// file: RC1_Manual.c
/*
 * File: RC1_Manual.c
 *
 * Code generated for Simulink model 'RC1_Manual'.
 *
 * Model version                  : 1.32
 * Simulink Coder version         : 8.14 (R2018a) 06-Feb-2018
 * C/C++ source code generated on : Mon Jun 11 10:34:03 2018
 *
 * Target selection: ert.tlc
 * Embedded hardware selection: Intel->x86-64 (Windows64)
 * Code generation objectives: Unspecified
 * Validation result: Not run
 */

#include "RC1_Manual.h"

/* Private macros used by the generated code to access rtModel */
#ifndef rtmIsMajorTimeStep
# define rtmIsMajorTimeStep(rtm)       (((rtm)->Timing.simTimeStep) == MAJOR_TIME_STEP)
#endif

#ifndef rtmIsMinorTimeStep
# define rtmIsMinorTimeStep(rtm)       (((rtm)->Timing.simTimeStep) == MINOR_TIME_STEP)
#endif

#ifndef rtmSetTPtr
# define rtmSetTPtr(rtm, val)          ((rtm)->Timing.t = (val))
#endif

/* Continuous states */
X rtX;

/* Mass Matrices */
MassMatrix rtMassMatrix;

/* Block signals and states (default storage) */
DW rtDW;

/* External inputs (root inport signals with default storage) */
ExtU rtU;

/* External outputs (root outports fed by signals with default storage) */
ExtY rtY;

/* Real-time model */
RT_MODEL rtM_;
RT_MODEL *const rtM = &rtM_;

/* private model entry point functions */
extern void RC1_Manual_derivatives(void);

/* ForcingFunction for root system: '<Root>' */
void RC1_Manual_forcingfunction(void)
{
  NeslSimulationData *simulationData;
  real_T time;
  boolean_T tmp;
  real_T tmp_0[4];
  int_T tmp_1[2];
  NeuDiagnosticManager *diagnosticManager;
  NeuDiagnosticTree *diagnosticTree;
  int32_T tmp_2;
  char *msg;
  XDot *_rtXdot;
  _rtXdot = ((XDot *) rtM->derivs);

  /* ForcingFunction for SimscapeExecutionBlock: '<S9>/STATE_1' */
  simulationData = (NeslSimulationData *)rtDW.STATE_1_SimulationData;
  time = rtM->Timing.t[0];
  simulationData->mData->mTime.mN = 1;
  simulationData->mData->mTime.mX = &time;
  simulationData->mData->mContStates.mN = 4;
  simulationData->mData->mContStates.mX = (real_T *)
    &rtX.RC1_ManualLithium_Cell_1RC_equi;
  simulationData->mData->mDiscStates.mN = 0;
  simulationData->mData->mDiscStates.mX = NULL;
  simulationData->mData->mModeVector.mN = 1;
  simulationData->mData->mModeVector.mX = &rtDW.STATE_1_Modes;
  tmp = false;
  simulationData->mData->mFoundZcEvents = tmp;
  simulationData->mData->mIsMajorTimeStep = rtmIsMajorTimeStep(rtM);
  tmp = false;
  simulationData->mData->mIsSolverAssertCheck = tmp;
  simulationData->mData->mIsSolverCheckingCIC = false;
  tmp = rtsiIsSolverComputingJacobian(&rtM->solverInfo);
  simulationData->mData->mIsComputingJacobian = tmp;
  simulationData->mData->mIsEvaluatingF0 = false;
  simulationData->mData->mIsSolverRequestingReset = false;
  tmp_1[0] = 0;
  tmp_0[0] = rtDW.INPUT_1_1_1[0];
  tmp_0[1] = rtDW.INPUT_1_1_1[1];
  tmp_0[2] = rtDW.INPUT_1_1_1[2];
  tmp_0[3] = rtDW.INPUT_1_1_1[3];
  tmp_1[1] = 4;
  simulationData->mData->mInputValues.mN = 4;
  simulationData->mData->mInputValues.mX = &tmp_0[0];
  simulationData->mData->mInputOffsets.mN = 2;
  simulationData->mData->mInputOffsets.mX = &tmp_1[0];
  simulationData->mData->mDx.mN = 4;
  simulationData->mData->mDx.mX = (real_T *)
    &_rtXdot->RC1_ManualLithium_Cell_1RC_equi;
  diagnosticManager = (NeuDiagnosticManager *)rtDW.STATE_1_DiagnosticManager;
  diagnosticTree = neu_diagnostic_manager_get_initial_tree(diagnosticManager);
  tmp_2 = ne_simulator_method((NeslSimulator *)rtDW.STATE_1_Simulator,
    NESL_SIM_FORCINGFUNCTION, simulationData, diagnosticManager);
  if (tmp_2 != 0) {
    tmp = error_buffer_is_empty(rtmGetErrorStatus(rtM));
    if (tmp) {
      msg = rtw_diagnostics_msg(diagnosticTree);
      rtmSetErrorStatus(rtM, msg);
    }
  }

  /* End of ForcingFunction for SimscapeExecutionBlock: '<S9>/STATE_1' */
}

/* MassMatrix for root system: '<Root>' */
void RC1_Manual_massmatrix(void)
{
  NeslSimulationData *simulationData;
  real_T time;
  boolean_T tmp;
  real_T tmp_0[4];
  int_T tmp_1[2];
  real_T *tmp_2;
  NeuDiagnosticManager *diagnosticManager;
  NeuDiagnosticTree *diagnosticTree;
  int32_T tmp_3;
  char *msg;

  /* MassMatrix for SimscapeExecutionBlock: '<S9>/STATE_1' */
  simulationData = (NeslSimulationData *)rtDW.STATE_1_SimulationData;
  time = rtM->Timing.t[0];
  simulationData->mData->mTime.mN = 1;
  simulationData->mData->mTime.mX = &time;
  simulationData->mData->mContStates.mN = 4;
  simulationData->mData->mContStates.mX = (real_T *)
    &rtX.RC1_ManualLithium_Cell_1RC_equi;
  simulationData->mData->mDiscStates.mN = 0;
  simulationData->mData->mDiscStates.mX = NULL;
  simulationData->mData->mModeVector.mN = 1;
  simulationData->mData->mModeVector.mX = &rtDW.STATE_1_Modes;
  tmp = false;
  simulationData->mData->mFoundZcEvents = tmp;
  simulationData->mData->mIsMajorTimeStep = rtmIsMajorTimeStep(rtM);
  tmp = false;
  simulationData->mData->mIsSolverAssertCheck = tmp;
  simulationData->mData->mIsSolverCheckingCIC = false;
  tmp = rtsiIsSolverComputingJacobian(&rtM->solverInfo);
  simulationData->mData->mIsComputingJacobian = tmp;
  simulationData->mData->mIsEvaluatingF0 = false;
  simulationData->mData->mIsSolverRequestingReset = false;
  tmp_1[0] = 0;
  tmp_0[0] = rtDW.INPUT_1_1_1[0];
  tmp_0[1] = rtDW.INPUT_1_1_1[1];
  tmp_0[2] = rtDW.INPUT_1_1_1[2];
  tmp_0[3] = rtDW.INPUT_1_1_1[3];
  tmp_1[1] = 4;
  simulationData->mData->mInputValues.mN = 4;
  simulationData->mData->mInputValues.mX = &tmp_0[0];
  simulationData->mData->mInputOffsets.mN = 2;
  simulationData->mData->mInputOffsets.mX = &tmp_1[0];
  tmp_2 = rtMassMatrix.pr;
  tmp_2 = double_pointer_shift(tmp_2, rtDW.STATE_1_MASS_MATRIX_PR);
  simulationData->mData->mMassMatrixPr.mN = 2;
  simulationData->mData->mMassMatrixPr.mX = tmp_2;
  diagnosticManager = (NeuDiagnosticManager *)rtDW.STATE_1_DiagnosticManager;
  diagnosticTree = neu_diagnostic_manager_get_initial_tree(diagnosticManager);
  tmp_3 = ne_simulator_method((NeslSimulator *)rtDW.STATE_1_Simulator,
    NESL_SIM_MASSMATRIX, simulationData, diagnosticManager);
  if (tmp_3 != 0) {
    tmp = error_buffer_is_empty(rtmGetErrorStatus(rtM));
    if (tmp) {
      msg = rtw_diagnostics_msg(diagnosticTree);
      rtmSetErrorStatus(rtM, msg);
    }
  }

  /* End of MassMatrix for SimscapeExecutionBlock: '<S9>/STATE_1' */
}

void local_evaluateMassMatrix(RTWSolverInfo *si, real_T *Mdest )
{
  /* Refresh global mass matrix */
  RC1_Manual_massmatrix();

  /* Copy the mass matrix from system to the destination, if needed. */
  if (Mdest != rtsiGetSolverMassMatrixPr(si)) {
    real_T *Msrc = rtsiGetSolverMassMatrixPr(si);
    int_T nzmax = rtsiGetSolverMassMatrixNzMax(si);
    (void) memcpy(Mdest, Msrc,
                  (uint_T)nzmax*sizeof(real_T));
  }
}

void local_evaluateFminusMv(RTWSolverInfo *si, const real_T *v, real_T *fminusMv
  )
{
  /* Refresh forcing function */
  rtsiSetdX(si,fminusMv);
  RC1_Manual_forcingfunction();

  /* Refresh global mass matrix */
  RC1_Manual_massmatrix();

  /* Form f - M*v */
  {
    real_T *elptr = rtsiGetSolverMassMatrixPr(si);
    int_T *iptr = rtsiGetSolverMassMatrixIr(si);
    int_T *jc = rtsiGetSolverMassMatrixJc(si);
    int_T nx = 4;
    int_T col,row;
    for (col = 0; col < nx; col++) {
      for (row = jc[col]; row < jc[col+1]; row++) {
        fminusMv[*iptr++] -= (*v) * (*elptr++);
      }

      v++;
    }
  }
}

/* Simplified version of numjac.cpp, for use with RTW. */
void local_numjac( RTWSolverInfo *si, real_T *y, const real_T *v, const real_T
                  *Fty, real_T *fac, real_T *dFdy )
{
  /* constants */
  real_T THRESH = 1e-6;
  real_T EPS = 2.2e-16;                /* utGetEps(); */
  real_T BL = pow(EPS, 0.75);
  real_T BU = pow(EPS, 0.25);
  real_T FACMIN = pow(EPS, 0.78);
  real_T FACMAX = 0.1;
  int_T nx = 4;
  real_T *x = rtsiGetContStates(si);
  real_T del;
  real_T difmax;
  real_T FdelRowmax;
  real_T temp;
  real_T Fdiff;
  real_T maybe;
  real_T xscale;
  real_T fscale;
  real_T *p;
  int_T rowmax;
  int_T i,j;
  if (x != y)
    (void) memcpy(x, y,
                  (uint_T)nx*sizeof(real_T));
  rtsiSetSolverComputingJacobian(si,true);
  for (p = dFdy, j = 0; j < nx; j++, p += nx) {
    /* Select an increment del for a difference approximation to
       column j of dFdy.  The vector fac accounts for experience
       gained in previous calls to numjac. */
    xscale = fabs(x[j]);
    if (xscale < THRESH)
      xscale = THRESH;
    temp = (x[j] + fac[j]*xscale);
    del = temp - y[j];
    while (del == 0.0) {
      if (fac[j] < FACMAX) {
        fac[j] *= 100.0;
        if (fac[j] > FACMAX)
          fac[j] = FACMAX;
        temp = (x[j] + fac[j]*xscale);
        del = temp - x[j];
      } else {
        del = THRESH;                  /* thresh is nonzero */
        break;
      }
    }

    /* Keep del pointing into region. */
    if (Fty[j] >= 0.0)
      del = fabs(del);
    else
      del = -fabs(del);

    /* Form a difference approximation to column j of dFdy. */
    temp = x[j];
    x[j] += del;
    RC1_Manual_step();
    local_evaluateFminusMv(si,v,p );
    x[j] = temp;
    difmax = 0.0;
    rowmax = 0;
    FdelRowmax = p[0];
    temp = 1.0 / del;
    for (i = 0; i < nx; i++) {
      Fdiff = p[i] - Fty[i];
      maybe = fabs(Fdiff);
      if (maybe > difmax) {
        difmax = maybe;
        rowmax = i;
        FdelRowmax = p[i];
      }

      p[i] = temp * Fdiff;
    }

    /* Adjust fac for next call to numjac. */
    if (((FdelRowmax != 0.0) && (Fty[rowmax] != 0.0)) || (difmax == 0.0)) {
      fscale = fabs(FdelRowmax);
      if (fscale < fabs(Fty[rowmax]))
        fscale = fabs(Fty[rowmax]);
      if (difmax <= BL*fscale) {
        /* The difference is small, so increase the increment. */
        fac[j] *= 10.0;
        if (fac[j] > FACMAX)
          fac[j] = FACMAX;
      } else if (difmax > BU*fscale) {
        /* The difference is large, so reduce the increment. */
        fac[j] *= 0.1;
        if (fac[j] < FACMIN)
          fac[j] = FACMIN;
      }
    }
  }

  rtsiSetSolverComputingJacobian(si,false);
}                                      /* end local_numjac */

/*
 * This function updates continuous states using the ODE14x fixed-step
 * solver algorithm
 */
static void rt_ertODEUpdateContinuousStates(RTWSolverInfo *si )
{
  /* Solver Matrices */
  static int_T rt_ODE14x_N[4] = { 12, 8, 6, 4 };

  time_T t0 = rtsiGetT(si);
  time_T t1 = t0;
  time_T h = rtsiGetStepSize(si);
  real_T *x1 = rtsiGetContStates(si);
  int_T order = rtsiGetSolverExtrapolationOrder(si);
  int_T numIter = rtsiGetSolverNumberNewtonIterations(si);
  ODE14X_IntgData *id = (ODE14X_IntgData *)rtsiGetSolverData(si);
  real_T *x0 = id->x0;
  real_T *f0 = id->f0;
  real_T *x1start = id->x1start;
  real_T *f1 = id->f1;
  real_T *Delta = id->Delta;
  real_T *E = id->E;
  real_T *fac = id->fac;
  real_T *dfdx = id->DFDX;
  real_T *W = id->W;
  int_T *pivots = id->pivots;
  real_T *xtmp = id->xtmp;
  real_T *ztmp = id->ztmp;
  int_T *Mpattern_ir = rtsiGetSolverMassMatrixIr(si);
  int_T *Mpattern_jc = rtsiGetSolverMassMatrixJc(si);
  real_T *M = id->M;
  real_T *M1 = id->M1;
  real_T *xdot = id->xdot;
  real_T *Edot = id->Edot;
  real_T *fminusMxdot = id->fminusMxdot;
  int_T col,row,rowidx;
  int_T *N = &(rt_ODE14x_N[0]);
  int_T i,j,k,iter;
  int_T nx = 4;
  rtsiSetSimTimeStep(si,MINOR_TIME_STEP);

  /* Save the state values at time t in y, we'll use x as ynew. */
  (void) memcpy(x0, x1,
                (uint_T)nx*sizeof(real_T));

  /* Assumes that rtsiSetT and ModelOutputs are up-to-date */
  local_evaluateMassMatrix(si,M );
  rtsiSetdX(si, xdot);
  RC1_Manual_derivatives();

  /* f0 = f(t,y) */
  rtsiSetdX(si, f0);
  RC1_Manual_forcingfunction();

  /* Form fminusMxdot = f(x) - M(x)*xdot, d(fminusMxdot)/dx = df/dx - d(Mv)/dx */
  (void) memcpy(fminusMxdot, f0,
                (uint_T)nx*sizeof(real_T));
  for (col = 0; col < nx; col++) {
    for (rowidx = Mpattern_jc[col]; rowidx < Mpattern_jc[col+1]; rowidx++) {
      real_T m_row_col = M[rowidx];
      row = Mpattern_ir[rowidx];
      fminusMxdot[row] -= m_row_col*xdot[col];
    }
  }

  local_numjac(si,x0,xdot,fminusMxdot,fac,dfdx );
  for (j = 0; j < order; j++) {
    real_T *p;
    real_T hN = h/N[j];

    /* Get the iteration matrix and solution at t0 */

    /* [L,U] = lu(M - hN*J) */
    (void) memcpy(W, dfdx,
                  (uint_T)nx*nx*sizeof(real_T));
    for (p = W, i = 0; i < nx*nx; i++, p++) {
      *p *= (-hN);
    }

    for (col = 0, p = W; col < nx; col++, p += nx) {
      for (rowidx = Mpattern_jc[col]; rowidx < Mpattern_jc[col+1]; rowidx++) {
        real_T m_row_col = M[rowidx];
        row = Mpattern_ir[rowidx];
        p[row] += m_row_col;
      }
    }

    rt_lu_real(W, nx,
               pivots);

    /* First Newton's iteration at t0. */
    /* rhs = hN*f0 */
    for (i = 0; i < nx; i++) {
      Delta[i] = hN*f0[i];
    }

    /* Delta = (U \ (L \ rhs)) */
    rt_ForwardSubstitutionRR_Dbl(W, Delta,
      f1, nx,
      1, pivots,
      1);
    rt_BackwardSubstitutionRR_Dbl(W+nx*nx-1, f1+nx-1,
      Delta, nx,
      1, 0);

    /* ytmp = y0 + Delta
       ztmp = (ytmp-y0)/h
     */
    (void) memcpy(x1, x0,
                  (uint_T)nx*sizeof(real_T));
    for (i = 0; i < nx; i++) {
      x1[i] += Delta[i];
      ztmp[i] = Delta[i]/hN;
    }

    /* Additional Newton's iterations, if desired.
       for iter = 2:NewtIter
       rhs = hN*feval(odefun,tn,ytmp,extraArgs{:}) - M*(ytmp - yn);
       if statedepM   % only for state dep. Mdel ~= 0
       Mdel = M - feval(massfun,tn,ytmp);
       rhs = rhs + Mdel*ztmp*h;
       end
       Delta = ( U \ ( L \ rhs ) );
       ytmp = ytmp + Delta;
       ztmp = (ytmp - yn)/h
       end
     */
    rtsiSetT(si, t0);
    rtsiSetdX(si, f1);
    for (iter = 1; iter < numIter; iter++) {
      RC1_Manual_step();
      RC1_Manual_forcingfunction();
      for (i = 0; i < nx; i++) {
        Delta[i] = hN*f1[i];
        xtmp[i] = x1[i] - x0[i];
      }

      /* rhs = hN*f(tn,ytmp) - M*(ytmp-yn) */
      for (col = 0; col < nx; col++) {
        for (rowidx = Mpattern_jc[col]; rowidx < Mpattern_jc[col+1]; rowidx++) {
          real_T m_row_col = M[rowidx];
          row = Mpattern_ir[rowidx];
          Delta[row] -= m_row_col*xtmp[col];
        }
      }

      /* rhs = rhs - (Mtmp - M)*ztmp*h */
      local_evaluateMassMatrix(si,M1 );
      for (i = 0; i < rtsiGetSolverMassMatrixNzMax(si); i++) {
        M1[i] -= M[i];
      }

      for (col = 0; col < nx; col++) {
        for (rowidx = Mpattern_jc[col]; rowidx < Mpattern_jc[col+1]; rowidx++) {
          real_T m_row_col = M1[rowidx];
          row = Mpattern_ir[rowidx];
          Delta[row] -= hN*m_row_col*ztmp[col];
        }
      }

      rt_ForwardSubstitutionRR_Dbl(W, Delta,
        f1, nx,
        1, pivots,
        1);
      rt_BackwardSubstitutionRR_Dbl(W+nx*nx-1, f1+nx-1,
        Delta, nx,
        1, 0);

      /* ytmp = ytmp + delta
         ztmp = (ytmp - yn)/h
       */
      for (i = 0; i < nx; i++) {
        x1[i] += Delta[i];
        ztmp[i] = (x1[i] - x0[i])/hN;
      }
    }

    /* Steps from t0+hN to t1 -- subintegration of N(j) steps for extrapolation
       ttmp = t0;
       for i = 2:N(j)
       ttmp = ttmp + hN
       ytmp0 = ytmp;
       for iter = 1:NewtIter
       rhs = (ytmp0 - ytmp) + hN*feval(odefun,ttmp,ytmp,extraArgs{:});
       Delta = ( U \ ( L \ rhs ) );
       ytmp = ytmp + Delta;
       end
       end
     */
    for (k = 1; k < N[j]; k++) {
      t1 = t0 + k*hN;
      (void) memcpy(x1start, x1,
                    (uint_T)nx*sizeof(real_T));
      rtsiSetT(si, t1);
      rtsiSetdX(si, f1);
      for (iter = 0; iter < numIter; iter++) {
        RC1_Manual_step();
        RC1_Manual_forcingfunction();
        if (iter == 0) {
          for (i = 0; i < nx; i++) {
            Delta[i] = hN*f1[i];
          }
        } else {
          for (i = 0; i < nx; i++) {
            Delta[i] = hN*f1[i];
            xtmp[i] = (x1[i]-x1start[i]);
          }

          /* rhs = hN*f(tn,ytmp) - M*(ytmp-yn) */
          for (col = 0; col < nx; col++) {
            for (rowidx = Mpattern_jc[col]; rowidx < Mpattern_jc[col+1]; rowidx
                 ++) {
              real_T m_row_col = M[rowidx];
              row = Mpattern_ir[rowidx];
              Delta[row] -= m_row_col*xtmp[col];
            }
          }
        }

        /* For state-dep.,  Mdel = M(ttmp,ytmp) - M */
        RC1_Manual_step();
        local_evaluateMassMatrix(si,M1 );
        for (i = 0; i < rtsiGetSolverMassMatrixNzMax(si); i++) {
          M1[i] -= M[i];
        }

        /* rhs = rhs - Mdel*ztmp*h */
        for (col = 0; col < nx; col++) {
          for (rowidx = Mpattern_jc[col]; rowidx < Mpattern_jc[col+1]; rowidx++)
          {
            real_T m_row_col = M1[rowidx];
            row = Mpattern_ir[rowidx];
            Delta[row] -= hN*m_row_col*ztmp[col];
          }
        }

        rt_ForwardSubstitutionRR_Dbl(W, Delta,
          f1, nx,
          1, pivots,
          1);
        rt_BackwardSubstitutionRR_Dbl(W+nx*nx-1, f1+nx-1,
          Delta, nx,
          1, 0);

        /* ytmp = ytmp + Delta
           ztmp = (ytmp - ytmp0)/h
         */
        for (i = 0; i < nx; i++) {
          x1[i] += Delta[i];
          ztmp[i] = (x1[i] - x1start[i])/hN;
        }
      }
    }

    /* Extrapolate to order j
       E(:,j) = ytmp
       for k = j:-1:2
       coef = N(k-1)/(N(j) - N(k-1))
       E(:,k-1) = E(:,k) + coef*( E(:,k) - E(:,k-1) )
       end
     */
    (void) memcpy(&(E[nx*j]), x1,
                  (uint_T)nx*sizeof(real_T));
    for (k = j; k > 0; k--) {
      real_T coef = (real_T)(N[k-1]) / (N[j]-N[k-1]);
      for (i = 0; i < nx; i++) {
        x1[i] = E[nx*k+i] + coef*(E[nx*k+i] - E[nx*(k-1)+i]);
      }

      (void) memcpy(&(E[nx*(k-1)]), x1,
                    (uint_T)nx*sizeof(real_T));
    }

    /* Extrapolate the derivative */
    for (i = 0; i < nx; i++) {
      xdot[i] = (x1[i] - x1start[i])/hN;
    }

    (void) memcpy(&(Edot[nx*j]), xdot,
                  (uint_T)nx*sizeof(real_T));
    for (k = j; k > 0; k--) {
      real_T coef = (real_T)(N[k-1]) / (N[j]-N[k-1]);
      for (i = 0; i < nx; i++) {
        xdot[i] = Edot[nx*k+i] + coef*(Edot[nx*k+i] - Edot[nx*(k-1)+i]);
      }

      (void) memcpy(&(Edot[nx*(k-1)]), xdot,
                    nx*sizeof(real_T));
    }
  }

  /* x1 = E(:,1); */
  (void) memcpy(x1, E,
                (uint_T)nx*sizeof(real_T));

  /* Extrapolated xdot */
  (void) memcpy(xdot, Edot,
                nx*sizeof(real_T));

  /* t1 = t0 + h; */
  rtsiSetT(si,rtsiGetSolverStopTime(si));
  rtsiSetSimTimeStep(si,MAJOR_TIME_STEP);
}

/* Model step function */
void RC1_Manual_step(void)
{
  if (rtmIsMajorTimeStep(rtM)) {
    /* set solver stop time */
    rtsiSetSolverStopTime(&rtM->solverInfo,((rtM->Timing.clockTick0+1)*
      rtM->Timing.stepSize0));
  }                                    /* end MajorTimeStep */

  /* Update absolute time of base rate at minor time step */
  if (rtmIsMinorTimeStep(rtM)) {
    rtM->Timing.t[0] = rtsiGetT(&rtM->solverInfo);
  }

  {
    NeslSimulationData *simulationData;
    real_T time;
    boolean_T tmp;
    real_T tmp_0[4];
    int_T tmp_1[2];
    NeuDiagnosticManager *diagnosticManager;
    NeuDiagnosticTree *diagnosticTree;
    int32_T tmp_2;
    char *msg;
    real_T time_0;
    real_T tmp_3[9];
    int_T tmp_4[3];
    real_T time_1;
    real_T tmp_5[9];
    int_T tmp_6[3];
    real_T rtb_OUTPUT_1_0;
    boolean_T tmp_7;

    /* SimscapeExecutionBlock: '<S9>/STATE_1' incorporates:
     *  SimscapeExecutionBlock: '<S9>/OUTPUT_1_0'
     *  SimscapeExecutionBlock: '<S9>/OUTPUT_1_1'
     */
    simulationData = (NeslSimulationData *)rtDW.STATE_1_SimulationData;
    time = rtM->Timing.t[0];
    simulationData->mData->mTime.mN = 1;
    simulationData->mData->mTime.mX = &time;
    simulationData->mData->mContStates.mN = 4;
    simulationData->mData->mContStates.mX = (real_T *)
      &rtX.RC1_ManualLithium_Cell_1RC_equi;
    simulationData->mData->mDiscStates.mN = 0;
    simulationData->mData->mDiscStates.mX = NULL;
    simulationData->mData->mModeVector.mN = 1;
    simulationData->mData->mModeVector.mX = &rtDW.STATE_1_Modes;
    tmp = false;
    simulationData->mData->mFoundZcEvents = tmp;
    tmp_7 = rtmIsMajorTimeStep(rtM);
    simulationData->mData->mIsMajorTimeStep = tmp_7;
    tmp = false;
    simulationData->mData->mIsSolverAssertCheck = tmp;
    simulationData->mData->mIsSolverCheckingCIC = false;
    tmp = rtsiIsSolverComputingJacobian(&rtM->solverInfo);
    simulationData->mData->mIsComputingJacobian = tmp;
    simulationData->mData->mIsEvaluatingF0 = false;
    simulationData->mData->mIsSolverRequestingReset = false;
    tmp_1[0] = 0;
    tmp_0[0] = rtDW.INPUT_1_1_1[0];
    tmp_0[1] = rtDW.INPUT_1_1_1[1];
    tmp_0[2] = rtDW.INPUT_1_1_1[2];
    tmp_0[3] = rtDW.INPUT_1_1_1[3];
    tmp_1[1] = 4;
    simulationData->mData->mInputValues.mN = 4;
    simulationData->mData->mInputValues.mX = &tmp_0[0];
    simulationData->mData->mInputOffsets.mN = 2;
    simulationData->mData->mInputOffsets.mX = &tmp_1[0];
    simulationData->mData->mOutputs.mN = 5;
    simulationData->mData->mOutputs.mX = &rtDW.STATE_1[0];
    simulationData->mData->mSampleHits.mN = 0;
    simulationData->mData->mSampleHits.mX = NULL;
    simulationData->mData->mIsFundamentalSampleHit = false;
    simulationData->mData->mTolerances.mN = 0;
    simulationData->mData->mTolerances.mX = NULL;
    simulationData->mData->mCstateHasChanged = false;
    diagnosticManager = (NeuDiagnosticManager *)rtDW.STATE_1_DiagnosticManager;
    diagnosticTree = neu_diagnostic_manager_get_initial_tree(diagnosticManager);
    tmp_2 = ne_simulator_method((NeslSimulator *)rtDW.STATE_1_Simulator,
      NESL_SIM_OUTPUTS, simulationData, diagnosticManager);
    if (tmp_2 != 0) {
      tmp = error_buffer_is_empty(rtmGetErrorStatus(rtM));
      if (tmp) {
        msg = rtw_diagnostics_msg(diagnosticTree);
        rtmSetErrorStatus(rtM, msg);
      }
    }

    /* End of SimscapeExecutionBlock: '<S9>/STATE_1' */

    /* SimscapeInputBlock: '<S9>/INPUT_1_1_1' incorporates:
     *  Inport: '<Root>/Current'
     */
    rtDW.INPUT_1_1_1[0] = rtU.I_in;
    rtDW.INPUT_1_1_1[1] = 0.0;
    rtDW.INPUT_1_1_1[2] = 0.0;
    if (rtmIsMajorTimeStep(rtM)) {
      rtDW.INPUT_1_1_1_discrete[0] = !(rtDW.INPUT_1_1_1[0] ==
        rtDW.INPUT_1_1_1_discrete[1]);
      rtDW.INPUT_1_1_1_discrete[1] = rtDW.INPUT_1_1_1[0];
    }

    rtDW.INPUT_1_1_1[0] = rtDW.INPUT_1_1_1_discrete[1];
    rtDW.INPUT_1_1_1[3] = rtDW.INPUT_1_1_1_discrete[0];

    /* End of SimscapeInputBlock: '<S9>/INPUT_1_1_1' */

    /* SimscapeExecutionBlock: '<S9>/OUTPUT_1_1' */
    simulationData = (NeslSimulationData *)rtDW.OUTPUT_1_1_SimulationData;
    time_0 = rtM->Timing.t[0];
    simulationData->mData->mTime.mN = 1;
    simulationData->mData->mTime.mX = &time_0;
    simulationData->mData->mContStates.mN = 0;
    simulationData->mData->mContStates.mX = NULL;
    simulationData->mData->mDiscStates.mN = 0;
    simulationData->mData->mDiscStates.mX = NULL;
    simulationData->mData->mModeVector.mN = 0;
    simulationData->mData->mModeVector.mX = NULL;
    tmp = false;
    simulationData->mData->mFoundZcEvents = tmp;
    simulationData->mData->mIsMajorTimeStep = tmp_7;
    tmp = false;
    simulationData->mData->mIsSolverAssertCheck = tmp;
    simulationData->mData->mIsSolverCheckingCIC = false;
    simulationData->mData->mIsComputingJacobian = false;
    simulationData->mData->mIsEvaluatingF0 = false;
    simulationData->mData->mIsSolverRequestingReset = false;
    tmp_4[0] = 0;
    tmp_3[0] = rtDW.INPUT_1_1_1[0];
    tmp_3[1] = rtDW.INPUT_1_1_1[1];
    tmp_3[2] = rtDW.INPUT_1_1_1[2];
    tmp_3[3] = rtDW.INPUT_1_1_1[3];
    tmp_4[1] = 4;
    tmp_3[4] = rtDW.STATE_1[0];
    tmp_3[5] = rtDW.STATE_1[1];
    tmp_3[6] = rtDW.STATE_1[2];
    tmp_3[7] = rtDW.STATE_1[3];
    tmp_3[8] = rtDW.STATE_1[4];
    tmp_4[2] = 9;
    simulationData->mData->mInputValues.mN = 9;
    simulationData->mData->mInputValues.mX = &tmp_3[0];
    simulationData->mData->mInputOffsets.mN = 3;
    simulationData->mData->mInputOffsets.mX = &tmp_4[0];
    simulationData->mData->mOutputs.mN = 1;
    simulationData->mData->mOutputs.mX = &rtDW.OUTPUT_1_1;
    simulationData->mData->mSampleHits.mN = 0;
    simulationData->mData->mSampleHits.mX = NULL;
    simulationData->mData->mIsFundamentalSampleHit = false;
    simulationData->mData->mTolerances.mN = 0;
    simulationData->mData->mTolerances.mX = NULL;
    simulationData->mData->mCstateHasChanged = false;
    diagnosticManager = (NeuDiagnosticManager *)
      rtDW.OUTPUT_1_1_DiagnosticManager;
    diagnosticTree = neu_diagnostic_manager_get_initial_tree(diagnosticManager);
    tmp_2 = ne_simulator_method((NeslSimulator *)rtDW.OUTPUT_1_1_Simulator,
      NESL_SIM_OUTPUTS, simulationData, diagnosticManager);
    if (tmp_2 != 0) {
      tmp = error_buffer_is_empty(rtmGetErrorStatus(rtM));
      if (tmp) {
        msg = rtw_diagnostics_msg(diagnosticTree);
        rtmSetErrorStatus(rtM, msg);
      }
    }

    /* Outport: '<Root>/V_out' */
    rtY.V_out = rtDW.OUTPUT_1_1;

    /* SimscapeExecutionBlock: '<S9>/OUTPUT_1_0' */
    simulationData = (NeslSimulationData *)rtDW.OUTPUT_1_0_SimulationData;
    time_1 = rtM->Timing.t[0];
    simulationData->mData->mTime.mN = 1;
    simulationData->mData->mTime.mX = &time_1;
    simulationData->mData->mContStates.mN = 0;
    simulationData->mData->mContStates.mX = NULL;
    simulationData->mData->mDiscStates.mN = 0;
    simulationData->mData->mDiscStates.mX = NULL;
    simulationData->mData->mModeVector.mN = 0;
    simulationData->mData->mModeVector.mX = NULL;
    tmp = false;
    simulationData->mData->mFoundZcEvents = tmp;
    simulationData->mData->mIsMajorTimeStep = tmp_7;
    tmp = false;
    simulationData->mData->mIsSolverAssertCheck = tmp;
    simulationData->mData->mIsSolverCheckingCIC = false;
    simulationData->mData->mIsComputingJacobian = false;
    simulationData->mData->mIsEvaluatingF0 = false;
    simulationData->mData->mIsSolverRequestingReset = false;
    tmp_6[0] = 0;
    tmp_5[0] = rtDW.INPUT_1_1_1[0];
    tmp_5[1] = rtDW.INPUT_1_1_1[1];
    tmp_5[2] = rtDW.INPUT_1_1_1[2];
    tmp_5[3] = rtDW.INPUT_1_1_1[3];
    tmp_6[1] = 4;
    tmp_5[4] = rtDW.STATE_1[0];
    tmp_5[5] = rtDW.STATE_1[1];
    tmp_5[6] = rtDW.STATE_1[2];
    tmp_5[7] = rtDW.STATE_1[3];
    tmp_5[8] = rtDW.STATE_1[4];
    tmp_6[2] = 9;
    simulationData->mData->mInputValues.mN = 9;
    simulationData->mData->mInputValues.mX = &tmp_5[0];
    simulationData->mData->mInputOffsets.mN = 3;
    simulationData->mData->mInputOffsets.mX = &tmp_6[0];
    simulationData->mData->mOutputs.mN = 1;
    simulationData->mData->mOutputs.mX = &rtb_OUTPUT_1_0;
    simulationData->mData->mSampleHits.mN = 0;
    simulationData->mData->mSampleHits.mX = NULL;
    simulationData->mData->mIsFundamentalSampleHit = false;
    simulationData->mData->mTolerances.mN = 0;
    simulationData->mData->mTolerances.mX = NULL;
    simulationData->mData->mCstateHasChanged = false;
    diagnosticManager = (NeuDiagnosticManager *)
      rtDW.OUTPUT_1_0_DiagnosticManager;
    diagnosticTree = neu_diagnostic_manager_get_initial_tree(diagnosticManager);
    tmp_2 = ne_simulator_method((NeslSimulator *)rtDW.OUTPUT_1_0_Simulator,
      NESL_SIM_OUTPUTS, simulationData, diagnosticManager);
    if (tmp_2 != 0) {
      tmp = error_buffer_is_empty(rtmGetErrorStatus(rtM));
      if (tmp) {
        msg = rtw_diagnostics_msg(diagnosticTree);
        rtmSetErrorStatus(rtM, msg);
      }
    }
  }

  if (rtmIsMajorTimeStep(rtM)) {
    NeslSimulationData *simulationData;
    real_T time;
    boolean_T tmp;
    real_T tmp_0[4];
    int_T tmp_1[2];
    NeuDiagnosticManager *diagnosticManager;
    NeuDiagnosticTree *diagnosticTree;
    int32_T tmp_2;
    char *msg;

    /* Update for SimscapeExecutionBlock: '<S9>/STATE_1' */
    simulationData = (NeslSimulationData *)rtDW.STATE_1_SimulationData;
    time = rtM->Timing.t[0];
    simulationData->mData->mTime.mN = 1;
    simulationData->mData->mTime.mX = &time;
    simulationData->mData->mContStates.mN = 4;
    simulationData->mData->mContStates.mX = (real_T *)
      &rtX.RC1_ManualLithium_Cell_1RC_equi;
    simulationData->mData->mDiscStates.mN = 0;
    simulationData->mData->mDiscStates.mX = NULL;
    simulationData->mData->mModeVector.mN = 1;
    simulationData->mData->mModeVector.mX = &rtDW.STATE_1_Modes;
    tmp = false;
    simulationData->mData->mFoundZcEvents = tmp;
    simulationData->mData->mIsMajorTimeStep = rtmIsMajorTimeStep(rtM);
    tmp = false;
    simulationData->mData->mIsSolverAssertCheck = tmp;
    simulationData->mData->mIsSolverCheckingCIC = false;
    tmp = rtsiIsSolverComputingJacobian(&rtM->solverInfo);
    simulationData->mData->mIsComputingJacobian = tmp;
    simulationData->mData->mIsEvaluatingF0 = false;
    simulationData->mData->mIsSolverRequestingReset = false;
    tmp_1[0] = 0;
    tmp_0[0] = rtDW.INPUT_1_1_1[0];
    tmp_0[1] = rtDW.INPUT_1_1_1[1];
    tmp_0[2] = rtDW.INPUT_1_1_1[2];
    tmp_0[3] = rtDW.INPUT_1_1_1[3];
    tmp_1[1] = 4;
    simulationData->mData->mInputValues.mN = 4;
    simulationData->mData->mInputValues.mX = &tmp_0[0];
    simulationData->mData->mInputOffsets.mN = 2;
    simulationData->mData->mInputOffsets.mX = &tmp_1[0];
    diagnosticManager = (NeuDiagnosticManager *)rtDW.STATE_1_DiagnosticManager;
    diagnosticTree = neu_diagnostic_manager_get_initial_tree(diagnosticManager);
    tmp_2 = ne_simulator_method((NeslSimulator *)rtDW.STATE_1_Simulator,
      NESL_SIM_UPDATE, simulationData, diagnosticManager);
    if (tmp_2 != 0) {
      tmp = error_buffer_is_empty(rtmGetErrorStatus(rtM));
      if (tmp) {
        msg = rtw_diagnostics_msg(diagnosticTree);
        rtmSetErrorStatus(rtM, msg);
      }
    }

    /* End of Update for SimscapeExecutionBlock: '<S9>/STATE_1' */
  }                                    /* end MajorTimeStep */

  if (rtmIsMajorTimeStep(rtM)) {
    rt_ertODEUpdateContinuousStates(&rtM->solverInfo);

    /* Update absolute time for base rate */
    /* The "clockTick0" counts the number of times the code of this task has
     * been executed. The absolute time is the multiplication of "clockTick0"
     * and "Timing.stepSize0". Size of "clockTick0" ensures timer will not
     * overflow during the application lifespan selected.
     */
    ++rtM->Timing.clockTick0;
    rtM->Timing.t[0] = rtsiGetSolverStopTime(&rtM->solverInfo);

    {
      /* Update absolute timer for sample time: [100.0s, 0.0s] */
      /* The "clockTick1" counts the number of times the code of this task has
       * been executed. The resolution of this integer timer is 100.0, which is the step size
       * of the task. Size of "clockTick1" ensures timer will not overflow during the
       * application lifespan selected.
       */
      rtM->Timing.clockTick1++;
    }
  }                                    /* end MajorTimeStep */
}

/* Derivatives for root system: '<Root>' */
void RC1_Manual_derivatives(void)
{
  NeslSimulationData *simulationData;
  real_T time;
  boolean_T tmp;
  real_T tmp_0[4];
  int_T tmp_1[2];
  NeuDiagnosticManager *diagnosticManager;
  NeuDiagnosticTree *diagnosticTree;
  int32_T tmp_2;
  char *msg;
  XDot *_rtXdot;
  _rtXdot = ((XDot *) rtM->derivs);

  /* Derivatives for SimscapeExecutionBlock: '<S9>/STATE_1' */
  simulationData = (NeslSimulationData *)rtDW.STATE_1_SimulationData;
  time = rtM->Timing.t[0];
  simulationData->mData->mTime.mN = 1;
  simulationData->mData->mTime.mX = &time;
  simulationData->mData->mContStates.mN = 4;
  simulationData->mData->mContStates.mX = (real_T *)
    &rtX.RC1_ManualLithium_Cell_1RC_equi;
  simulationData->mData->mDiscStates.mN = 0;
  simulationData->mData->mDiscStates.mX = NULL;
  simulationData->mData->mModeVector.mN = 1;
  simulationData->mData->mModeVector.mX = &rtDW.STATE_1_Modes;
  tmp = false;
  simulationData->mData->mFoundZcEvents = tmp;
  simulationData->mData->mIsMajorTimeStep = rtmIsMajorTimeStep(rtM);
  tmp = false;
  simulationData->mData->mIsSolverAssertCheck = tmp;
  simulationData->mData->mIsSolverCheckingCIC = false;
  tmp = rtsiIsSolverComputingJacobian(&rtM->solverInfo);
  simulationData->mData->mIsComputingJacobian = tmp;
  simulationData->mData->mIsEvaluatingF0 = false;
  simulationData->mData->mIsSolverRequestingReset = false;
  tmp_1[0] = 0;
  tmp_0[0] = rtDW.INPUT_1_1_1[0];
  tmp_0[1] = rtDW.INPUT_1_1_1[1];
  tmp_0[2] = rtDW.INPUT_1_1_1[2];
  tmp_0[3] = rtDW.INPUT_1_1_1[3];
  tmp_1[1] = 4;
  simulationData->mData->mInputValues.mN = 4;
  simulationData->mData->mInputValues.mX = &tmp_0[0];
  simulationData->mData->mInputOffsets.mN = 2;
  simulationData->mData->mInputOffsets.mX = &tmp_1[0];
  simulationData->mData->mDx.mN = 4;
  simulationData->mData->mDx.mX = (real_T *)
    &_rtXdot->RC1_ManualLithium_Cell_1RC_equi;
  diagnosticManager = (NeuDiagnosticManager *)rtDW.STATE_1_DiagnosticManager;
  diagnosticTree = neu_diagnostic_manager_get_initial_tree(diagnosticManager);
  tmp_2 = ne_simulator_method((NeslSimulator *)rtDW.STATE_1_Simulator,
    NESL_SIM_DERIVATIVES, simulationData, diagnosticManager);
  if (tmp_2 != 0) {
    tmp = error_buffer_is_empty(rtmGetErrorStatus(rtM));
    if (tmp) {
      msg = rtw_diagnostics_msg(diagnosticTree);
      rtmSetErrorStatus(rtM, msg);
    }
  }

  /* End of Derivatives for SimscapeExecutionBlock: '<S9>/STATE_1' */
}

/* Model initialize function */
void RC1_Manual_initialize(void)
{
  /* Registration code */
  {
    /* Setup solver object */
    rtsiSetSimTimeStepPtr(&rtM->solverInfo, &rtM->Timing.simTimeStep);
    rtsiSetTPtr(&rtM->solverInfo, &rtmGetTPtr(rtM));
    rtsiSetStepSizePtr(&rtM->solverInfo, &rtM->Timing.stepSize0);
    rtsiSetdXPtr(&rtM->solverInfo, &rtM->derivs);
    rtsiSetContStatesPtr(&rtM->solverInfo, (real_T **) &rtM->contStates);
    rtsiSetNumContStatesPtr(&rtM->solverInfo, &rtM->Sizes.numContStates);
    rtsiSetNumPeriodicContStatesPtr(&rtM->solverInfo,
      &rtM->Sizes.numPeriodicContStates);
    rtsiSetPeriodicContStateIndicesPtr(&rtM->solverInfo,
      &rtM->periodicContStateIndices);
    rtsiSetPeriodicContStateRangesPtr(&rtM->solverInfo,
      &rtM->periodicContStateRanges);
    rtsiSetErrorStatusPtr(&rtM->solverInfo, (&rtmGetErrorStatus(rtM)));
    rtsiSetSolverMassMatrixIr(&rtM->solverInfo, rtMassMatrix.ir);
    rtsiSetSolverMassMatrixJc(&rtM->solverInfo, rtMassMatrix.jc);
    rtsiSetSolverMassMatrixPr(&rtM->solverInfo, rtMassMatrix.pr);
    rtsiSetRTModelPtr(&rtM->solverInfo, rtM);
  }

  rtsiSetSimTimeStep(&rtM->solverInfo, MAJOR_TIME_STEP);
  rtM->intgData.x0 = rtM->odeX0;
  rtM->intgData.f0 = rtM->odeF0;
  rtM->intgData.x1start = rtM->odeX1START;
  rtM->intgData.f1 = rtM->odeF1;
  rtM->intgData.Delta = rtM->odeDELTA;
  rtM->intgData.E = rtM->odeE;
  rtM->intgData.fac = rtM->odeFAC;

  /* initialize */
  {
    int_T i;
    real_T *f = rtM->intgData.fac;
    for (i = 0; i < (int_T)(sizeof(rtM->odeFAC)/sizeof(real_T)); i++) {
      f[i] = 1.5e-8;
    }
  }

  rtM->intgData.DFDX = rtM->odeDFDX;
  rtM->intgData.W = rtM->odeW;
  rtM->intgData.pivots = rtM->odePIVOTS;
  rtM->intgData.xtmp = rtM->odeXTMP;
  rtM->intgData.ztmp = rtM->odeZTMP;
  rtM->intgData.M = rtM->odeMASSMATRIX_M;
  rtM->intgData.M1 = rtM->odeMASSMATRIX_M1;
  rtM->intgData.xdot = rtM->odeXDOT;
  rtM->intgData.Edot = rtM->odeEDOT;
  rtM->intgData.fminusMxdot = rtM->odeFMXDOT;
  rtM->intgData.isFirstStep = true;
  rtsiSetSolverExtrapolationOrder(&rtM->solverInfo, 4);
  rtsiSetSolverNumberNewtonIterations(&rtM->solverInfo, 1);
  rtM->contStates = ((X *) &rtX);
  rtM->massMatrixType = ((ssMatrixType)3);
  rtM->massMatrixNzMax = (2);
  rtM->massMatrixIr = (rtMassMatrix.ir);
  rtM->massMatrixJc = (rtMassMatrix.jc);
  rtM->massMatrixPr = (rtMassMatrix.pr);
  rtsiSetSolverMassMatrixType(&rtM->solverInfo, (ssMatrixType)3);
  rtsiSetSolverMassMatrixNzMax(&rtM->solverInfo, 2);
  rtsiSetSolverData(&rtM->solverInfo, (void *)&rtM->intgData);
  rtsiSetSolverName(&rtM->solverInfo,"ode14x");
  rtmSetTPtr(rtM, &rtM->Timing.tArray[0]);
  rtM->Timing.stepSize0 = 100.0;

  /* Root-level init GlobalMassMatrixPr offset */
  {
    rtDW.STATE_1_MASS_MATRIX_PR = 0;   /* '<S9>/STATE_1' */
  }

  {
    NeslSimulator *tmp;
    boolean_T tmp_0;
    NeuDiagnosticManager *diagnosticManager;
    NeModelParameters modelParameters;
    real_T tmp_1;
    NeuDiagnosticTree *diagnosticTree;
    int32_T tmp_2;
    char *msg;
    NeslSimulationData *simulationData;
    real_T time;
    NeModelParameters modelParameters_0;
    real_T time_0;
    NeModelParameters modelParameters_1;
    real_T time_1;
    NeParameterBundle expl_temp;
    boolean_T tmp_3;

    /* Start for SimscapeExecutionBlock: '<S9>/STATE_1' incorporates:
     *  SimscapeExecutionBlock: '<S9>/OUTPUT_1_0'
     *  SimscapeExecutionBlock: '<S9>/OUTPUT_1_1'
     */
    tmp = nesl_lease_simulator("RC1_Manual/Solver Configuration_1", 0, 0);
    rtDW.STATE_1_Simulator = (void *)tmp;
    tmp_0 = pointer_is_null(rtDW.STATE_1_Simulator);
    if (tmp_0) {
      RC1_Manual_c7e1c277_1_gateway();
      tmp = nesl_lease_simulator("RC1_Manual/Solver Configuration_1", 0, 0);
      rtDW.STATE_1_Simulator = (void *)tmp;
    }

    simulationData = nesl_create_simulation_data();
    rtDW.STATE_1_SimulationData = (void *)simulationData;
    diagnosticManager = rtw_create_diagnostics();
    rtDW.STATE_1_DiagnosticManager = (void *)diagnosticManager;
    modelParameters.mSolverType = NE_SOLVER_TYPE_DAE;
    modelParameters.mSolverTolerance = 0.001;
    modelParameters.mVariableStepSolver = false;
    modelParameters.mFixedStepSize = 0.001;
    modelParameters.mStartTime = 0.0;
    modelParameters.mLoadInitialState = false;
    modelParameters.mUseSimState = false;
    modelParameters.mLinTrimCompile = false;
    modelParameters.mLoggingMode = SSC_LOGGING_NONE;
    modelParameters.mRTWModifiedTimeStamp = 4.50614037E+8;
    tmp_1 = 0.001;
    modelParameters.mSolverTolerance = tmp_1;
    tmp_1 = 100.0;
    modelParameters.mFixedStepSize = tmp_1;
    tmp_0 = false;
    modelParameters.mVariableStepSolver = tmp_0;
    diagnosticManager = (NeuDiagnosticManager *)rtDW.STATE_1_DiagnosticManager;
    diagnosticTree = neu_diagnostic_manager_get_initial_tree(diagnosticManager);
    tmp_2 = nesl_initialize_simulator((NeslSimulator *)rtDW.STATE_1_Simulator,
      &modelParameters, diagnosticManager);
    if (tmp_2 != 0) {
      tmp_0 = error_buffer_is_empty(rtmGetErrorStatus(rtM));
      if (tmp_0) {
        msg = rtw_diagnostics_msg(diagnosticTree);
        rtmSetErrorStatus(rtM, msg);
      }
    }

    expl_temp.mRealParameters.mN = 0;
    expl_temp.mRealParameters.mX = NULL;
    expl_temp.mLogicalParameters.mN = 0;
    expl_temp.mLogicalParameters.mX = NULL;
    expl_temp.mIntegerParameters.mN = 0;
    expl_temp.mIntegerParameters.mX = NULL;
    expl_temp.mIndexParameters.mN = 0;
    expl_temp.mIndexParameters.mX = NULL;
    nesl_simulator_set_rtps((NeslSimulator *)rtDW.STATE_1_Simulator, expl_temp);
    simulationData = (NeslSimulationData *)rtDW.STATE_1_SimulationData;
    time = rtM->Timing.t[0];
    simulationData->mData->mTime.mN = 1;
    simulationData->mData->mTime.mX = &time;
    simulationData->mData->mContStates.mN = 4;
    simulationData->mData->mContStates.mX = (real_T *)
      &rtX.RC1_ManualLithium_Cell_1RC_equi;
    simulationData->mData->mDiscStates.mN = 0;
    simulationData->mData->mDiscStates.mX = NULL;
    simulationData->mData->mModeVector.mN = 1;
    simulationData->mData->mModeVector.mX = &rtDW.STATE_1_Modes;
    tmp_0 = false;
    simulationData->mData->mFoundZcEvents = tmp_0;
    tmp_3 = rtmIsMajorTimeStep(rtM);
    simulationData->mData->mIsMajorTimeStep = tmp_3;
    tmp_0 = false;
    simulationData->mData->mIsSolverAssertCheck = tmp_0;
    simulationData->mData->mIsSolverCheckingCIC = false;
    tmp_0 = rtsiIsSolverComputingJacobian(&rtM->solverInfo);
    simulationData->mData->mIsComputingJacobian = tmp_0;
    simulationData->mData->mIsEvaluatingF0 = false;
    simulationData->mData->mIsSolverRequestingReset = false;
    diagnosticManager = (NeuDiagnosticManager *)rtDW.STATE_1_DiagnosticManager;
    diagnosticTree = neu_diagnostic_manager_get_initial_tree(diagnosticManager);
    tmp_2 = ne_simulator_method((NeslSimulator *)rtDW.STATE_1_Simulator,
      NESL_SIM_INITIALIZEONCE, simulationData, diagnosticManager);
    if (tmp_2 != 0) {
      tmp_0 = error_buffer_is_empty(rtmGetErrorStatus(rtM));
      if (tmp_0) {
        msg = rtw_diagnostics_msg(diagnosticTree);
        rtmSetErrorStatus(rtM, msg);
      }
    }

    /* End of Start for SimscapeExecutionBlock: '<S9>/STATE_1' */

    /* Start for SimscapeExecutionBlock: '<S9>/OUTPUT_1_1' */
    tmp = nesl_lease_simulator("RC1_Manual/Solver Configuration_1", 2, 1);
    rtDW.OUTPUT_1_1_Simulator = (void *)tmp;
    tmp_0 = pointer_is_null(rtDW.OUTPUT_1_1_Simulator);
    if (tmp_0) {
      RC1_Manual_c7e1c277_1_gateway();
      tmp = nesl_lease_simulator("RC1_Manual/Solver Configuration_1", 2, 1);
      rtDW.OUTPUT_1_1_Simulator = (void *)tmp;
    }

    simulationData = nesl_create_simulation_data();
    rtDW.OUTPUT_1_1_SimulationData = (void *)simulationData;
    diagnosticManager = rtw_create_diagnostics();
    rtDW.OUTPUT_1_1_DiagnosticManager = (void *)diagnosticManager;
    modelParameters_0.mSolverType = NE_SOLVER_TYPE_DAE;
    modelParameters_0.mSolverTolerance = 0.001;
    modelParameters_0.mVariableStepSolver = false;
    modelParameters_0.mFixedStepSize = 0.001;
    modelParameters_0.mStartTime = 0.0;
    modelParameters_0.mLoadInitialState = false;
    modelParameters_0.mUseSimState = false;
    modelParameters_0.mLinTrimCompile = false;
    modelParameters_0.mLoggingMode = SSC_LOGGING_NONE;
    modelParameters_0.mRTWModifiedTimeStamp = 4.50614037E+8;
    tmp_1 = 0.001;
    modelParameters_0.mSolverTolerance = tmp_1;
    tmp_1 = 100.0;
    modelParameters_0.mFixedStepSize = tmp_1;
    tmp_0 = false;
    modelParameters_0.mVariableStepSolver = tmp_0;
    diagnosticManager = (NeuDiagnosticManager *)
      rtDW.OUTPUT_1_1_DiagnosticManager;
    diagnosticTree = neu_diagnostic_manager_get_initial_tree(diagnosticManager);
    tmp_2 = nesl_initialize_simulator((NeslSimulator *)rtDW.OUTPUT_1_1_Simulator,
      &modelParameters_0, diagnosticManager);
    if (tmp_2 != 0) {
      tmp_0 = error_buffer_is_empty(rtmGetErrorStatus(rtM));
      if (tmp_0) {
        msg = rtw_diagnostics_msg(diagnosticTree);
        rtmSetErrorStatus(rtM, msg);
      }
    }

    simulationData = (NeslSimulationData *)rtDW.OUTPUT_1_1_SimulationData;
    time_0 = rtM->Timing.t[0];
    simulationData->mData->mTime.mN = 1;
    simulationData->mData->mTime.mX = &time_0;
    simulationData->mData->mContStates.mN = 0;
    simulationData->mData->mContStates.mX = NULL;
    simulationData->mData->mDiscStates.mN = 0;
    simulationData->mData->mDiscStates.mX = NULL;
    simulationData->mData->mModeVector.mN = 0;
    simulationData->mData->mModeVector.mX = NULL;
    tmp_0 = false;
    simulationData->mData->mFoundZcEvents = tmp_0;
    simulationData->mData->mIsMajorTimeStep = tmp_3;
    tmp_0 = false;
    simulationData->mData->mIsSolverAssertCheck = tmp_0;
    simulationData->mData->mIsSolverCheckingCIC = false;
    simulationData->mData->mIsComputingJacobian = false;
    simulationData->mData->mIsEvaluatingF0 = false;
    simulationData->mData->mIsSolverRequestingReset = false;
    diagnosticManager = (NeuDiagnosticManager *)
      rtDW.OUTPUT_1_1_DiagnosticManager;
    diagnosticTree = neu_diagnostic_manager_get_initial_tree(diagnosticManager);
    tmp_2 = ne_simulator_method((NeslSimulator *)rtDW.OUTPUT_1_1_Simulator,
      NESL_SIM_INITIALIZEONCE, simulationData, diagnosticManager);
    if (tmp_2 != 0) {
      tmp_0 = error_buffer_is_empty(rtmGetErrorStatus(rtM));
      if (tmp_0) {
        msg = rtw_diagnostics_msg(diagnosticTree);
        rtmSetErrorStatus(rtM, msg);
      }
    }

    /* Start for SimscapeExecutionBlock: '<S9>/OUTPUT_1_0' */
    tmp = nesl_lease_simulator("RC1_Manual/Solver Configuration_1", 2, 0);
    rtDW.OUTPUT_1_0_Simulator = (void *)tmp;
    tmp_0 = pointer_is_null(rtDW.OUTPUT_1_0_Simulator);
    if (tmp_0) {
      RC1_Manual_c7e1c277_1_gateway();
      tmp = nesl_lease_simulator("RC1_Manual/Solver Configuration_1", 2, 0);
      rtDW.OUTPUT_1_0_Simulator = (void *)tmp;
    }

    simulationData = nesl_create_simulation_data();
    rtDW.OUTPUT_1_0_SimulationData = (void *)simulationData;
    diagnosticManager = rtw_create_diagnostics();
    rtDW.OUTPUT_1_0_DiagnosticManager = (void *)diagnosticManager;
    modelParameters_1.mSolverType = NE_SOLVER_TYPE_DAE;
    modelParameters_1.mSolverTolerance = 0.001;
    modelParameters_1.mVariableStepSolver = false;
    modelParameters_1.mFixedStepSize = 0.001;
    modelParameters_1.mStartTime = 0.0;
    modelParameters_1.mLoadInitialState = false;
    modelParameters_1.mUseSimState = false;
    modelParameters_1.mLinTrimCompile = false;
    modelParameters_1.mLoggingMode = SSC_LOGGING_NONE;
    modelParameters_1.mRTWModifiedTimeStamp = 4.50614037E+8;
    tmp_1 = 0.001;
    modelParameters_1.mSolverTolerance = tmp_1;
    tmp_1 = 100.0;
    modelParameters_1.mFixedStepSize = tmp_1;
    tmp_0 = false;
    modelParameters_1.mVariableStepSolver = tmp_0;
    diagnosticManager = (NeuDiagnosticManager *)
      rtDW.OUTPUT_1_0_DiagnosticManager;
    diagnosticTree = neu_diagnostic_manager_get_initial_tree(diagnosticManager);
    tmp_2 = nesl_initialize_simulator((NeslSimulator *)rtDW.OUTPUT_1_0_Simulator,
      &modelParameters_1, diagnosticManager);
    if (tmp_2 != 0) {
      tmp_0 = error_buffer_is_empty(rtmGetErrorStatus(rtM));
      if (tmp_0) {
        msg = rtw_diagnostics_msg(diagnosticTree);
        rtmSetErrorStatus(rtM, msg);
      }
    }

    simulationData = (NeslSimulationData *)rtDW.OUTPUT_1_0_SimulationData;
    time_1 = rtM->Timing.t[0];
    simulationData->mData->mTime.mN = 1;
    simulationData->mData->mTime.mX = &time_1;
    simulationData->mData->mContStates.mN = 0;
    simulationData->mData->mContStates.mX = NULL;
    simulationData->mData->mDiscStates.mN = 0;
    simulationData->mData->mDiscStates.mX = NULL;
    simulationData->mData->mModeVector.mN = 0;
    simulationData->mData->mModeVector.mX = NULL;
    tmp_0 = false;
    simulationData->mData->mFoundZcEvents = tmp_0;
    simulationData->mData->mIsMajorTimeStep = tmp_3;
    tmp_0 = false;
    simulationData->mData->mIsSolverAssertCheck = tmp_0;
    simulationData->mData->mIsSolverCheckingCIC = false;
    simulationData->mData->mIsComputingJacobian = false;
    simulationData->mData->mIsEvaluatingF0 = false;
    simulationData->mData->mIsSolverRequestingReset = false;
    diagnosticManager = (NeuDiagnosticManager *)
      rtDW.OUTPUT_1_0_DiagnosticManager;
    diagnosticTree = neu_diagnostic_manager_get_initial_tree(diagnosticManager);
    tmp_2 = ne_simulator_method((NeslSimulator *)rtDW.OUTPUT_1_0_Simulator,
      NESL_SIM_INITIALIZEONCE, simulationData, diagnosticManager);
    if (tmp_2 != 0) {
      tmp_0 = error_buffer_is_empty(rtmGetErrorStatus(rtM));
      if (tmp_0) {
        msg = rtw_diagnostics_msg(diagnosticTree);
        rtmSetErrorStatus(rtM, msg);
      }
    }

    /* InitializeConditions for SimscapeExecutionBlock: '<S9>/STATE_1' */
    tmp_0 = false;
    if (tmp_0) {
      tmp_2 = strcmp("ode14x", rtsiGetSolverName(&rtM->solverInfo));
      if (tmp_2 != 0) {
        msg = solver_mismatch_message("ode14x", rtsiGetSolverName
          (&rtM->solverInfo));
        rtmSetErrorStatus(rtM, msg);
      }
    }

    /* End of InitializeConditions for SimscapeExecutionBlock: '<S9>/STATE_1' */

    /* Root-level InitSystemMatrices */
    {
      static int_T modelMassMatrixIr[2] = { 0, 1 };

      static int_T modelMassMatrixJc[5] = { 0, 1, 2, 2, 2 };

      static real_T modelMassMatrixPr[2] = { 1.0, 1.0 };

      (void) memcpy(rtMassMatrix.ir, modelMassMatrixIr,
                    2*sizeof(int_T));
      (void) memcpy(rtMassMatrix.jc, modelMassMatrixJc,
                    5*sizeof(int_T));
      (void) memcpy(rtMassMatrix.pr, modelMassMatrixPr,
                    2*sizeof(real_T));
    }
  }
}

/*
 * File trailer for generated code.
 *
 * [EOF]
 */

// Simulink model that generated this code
simulink model "RC1_Manual"  (R2017b)
settings: Solver=ode23t  StartTime=0.0  StopTime=5000  RelTol=1e-3  EnableMultiTasking=on
values from neighbouring files (symbols this model uses):
  Capacity = 31    [RC1_Manual.mat]    (also in dataInit.m; mayBeUsed.mat)
libraries: LiBatteryElements_lib x4, nesl_utility x4, fl_lib x3

== system RC1_Manual ==
  Current : Inport
  Bus Creator : BusCreator  Inputs=2
  Controlled Current Source : fl_lib/Electrical/Electrical Sources/Controlled Current Source
  Electrical Reference : fl_lib/Electrical/Electrical Elements/Electrical Reference
  From Workspace : FromWorkspace  VariableName=[t,V_out]  SampleTime=0
  "Lithium Cell (1RC equivalent circuit model, single temperature)" : Subsystem
  PS-Simulink Converter1 : nesl_utility/PS-Simulink Converter  PhysicalDomain=network_engine_domain  SubClassName=ps_output  LeftPortType=input  RightPortType=output  PseudoPeriodic=off  Frequencies=[]  Unit=V  AffineConversion=off
  PS-Simulink Converter2 : nesl_utility/PS-Simulink Converter  PhysicalDomain=network_engine_domain  SubClassName=ps_output  LeftPortType=input  RightPortType=output  PseudoPeriodic=off  Frequencies=[]  Unit=1  AffineConversion=off
  Scope : Scope  NumInputPorts=3
  Scope1 : Scope
  Simulink-PS Converter1 : nesl_utility/Simulink-PS Converter  PhysicalDomain=network_engine_domain  SubClassName=ps_input  LeftPortType=input  RightPortType=output  PseudoPeriodic=off  Frequencies=[]  NoiseDistribution=none  NoiseParameters=[]  Unit=A  AffineConversion=off  FilteringAndDerivatives=zero  SimscapeFilterOrder=1  InputFilterTimeConstant=.001  UdotUserProvided=0
  Solver Configuration : nesl_utility/Solver Configuration  PhysicalDomain=network_engine_domain  SubClassName=solver  LeftPortType=input  RightPortType=generic  Accelerate=off  Tones=[]  Harmonics=[]  SimulateNoise=off  Profile=off  UseLocalSampling=off  EnableSwitchedLinearOptims=on  FrequencyDomain=off  UseCCode=off  RelTol=0.001  AbsTol=1e-06  MinStep=1e-09  ToWorkspace=off  RevertToSquareIcSolve=off  NumHomotopyIterations=100  PhasorMode=off  PhasorModeNumHarmonics=1  DoDC=off  ResidualTolerance=1e-09  UseLocalSolver=off  LocalSolverChoice=NE_BACKWARD_EULER_ADVANCER  LocalSolverSampleTime=0.001  DoFixedCost=off  MaxNonlinIter=3  MaxModeIter=2  LinearAlgebra=Sparse  DelaysMemoryBudget=1024  AutomaticFiltering=on  FilteringTimeConstant=0.001
  Terminator : Terminator
  Voltage Sensor : fl_lib/Electrical/Electrical Sensors/Voltage Sensor
  V_out : Outport
  wires:
  PS-Simulink Converter1/1 -> Bus Creator/1, Scope/3, V_out/1  "V_out"
  PS-Simulink Converter2/1 -> Terminator/1, Scope/2
  Current/1 -> Scope/1, Simulink-PS Converter1/1  "I_in"
  From Workspace/1 -> Bus Creator/2
  Bus Creator/1 -> Scope1/1
  connections:
  Solver Configuration/RConn1 -- Controlled Current Source/LConn1 -- "Lithium Cell (1RC equivalent circuit model, single temperature)"/LConn1 -- Voltage Sensor/LConn1
  Controlled Current Source/RConn1 -- Simulink-PS Converter1/RConn1
  Controlled Current Source/RConn2 -- Electrical Reference/LConn1 -- Voltage Sensor/RConn2 -- "Lithium Cell (1RC equivalent circuit model, single temperature)"/RConn1
  Voltage Sensor/RConn1 -- PS-Simulink Converter1/LConn1
  "Lithium Cell (1RC equivalent circuit model, single temperature)"/LConn2 -- PS-Simulink Converter2/LConn1

== system RC1_Manual/Lithium Cell (1RC equivalent circuit model, single temperature) ==
  C1 : LiBatteryElements_lib/C_table_1Temp  C_Table=C1 F  SOC_Table=SOC_LUT  v0=0 V
  Em : LiBatteryElements_lib/Em_table_1Temp  Em_Table=Em V  SOC_Table=SOC_LUT  C=Capacity hr*A  Qinit=Qe_init hr*A
  R0 : LiBatteryElements_lib/R_table_1Temp  R_Table=R0 Ohm  SOC_Table=SOC_LUT
  R1 : LiBatteryElements_lib/R_table_1Temp  R_Table=R1 Ohm  SOC_Table=SOC_LUT
  + : PMIOPort  Tag=PMCPort  Port=1  Side=Left
  - : PMIOPort  Tag=PMCPort  Port=2  Side=Right
  SOC : PMIOPort  Tag=PMCPort  Port=3  Side=Left
  connections:
  Em/LConn1 -- C1/LConn1 -- R1/LConn1
  +/RConn1 -- R0/RConn1
  Em/RConn1 -- -/RConn1
  R0/LConn2 -- SOC/RConn1 -- C1/LConn2 -- R1/LConn2 -- Em/LConn2
  R1/RConn1 -- R0/LConn1 -- C1/RConn1
